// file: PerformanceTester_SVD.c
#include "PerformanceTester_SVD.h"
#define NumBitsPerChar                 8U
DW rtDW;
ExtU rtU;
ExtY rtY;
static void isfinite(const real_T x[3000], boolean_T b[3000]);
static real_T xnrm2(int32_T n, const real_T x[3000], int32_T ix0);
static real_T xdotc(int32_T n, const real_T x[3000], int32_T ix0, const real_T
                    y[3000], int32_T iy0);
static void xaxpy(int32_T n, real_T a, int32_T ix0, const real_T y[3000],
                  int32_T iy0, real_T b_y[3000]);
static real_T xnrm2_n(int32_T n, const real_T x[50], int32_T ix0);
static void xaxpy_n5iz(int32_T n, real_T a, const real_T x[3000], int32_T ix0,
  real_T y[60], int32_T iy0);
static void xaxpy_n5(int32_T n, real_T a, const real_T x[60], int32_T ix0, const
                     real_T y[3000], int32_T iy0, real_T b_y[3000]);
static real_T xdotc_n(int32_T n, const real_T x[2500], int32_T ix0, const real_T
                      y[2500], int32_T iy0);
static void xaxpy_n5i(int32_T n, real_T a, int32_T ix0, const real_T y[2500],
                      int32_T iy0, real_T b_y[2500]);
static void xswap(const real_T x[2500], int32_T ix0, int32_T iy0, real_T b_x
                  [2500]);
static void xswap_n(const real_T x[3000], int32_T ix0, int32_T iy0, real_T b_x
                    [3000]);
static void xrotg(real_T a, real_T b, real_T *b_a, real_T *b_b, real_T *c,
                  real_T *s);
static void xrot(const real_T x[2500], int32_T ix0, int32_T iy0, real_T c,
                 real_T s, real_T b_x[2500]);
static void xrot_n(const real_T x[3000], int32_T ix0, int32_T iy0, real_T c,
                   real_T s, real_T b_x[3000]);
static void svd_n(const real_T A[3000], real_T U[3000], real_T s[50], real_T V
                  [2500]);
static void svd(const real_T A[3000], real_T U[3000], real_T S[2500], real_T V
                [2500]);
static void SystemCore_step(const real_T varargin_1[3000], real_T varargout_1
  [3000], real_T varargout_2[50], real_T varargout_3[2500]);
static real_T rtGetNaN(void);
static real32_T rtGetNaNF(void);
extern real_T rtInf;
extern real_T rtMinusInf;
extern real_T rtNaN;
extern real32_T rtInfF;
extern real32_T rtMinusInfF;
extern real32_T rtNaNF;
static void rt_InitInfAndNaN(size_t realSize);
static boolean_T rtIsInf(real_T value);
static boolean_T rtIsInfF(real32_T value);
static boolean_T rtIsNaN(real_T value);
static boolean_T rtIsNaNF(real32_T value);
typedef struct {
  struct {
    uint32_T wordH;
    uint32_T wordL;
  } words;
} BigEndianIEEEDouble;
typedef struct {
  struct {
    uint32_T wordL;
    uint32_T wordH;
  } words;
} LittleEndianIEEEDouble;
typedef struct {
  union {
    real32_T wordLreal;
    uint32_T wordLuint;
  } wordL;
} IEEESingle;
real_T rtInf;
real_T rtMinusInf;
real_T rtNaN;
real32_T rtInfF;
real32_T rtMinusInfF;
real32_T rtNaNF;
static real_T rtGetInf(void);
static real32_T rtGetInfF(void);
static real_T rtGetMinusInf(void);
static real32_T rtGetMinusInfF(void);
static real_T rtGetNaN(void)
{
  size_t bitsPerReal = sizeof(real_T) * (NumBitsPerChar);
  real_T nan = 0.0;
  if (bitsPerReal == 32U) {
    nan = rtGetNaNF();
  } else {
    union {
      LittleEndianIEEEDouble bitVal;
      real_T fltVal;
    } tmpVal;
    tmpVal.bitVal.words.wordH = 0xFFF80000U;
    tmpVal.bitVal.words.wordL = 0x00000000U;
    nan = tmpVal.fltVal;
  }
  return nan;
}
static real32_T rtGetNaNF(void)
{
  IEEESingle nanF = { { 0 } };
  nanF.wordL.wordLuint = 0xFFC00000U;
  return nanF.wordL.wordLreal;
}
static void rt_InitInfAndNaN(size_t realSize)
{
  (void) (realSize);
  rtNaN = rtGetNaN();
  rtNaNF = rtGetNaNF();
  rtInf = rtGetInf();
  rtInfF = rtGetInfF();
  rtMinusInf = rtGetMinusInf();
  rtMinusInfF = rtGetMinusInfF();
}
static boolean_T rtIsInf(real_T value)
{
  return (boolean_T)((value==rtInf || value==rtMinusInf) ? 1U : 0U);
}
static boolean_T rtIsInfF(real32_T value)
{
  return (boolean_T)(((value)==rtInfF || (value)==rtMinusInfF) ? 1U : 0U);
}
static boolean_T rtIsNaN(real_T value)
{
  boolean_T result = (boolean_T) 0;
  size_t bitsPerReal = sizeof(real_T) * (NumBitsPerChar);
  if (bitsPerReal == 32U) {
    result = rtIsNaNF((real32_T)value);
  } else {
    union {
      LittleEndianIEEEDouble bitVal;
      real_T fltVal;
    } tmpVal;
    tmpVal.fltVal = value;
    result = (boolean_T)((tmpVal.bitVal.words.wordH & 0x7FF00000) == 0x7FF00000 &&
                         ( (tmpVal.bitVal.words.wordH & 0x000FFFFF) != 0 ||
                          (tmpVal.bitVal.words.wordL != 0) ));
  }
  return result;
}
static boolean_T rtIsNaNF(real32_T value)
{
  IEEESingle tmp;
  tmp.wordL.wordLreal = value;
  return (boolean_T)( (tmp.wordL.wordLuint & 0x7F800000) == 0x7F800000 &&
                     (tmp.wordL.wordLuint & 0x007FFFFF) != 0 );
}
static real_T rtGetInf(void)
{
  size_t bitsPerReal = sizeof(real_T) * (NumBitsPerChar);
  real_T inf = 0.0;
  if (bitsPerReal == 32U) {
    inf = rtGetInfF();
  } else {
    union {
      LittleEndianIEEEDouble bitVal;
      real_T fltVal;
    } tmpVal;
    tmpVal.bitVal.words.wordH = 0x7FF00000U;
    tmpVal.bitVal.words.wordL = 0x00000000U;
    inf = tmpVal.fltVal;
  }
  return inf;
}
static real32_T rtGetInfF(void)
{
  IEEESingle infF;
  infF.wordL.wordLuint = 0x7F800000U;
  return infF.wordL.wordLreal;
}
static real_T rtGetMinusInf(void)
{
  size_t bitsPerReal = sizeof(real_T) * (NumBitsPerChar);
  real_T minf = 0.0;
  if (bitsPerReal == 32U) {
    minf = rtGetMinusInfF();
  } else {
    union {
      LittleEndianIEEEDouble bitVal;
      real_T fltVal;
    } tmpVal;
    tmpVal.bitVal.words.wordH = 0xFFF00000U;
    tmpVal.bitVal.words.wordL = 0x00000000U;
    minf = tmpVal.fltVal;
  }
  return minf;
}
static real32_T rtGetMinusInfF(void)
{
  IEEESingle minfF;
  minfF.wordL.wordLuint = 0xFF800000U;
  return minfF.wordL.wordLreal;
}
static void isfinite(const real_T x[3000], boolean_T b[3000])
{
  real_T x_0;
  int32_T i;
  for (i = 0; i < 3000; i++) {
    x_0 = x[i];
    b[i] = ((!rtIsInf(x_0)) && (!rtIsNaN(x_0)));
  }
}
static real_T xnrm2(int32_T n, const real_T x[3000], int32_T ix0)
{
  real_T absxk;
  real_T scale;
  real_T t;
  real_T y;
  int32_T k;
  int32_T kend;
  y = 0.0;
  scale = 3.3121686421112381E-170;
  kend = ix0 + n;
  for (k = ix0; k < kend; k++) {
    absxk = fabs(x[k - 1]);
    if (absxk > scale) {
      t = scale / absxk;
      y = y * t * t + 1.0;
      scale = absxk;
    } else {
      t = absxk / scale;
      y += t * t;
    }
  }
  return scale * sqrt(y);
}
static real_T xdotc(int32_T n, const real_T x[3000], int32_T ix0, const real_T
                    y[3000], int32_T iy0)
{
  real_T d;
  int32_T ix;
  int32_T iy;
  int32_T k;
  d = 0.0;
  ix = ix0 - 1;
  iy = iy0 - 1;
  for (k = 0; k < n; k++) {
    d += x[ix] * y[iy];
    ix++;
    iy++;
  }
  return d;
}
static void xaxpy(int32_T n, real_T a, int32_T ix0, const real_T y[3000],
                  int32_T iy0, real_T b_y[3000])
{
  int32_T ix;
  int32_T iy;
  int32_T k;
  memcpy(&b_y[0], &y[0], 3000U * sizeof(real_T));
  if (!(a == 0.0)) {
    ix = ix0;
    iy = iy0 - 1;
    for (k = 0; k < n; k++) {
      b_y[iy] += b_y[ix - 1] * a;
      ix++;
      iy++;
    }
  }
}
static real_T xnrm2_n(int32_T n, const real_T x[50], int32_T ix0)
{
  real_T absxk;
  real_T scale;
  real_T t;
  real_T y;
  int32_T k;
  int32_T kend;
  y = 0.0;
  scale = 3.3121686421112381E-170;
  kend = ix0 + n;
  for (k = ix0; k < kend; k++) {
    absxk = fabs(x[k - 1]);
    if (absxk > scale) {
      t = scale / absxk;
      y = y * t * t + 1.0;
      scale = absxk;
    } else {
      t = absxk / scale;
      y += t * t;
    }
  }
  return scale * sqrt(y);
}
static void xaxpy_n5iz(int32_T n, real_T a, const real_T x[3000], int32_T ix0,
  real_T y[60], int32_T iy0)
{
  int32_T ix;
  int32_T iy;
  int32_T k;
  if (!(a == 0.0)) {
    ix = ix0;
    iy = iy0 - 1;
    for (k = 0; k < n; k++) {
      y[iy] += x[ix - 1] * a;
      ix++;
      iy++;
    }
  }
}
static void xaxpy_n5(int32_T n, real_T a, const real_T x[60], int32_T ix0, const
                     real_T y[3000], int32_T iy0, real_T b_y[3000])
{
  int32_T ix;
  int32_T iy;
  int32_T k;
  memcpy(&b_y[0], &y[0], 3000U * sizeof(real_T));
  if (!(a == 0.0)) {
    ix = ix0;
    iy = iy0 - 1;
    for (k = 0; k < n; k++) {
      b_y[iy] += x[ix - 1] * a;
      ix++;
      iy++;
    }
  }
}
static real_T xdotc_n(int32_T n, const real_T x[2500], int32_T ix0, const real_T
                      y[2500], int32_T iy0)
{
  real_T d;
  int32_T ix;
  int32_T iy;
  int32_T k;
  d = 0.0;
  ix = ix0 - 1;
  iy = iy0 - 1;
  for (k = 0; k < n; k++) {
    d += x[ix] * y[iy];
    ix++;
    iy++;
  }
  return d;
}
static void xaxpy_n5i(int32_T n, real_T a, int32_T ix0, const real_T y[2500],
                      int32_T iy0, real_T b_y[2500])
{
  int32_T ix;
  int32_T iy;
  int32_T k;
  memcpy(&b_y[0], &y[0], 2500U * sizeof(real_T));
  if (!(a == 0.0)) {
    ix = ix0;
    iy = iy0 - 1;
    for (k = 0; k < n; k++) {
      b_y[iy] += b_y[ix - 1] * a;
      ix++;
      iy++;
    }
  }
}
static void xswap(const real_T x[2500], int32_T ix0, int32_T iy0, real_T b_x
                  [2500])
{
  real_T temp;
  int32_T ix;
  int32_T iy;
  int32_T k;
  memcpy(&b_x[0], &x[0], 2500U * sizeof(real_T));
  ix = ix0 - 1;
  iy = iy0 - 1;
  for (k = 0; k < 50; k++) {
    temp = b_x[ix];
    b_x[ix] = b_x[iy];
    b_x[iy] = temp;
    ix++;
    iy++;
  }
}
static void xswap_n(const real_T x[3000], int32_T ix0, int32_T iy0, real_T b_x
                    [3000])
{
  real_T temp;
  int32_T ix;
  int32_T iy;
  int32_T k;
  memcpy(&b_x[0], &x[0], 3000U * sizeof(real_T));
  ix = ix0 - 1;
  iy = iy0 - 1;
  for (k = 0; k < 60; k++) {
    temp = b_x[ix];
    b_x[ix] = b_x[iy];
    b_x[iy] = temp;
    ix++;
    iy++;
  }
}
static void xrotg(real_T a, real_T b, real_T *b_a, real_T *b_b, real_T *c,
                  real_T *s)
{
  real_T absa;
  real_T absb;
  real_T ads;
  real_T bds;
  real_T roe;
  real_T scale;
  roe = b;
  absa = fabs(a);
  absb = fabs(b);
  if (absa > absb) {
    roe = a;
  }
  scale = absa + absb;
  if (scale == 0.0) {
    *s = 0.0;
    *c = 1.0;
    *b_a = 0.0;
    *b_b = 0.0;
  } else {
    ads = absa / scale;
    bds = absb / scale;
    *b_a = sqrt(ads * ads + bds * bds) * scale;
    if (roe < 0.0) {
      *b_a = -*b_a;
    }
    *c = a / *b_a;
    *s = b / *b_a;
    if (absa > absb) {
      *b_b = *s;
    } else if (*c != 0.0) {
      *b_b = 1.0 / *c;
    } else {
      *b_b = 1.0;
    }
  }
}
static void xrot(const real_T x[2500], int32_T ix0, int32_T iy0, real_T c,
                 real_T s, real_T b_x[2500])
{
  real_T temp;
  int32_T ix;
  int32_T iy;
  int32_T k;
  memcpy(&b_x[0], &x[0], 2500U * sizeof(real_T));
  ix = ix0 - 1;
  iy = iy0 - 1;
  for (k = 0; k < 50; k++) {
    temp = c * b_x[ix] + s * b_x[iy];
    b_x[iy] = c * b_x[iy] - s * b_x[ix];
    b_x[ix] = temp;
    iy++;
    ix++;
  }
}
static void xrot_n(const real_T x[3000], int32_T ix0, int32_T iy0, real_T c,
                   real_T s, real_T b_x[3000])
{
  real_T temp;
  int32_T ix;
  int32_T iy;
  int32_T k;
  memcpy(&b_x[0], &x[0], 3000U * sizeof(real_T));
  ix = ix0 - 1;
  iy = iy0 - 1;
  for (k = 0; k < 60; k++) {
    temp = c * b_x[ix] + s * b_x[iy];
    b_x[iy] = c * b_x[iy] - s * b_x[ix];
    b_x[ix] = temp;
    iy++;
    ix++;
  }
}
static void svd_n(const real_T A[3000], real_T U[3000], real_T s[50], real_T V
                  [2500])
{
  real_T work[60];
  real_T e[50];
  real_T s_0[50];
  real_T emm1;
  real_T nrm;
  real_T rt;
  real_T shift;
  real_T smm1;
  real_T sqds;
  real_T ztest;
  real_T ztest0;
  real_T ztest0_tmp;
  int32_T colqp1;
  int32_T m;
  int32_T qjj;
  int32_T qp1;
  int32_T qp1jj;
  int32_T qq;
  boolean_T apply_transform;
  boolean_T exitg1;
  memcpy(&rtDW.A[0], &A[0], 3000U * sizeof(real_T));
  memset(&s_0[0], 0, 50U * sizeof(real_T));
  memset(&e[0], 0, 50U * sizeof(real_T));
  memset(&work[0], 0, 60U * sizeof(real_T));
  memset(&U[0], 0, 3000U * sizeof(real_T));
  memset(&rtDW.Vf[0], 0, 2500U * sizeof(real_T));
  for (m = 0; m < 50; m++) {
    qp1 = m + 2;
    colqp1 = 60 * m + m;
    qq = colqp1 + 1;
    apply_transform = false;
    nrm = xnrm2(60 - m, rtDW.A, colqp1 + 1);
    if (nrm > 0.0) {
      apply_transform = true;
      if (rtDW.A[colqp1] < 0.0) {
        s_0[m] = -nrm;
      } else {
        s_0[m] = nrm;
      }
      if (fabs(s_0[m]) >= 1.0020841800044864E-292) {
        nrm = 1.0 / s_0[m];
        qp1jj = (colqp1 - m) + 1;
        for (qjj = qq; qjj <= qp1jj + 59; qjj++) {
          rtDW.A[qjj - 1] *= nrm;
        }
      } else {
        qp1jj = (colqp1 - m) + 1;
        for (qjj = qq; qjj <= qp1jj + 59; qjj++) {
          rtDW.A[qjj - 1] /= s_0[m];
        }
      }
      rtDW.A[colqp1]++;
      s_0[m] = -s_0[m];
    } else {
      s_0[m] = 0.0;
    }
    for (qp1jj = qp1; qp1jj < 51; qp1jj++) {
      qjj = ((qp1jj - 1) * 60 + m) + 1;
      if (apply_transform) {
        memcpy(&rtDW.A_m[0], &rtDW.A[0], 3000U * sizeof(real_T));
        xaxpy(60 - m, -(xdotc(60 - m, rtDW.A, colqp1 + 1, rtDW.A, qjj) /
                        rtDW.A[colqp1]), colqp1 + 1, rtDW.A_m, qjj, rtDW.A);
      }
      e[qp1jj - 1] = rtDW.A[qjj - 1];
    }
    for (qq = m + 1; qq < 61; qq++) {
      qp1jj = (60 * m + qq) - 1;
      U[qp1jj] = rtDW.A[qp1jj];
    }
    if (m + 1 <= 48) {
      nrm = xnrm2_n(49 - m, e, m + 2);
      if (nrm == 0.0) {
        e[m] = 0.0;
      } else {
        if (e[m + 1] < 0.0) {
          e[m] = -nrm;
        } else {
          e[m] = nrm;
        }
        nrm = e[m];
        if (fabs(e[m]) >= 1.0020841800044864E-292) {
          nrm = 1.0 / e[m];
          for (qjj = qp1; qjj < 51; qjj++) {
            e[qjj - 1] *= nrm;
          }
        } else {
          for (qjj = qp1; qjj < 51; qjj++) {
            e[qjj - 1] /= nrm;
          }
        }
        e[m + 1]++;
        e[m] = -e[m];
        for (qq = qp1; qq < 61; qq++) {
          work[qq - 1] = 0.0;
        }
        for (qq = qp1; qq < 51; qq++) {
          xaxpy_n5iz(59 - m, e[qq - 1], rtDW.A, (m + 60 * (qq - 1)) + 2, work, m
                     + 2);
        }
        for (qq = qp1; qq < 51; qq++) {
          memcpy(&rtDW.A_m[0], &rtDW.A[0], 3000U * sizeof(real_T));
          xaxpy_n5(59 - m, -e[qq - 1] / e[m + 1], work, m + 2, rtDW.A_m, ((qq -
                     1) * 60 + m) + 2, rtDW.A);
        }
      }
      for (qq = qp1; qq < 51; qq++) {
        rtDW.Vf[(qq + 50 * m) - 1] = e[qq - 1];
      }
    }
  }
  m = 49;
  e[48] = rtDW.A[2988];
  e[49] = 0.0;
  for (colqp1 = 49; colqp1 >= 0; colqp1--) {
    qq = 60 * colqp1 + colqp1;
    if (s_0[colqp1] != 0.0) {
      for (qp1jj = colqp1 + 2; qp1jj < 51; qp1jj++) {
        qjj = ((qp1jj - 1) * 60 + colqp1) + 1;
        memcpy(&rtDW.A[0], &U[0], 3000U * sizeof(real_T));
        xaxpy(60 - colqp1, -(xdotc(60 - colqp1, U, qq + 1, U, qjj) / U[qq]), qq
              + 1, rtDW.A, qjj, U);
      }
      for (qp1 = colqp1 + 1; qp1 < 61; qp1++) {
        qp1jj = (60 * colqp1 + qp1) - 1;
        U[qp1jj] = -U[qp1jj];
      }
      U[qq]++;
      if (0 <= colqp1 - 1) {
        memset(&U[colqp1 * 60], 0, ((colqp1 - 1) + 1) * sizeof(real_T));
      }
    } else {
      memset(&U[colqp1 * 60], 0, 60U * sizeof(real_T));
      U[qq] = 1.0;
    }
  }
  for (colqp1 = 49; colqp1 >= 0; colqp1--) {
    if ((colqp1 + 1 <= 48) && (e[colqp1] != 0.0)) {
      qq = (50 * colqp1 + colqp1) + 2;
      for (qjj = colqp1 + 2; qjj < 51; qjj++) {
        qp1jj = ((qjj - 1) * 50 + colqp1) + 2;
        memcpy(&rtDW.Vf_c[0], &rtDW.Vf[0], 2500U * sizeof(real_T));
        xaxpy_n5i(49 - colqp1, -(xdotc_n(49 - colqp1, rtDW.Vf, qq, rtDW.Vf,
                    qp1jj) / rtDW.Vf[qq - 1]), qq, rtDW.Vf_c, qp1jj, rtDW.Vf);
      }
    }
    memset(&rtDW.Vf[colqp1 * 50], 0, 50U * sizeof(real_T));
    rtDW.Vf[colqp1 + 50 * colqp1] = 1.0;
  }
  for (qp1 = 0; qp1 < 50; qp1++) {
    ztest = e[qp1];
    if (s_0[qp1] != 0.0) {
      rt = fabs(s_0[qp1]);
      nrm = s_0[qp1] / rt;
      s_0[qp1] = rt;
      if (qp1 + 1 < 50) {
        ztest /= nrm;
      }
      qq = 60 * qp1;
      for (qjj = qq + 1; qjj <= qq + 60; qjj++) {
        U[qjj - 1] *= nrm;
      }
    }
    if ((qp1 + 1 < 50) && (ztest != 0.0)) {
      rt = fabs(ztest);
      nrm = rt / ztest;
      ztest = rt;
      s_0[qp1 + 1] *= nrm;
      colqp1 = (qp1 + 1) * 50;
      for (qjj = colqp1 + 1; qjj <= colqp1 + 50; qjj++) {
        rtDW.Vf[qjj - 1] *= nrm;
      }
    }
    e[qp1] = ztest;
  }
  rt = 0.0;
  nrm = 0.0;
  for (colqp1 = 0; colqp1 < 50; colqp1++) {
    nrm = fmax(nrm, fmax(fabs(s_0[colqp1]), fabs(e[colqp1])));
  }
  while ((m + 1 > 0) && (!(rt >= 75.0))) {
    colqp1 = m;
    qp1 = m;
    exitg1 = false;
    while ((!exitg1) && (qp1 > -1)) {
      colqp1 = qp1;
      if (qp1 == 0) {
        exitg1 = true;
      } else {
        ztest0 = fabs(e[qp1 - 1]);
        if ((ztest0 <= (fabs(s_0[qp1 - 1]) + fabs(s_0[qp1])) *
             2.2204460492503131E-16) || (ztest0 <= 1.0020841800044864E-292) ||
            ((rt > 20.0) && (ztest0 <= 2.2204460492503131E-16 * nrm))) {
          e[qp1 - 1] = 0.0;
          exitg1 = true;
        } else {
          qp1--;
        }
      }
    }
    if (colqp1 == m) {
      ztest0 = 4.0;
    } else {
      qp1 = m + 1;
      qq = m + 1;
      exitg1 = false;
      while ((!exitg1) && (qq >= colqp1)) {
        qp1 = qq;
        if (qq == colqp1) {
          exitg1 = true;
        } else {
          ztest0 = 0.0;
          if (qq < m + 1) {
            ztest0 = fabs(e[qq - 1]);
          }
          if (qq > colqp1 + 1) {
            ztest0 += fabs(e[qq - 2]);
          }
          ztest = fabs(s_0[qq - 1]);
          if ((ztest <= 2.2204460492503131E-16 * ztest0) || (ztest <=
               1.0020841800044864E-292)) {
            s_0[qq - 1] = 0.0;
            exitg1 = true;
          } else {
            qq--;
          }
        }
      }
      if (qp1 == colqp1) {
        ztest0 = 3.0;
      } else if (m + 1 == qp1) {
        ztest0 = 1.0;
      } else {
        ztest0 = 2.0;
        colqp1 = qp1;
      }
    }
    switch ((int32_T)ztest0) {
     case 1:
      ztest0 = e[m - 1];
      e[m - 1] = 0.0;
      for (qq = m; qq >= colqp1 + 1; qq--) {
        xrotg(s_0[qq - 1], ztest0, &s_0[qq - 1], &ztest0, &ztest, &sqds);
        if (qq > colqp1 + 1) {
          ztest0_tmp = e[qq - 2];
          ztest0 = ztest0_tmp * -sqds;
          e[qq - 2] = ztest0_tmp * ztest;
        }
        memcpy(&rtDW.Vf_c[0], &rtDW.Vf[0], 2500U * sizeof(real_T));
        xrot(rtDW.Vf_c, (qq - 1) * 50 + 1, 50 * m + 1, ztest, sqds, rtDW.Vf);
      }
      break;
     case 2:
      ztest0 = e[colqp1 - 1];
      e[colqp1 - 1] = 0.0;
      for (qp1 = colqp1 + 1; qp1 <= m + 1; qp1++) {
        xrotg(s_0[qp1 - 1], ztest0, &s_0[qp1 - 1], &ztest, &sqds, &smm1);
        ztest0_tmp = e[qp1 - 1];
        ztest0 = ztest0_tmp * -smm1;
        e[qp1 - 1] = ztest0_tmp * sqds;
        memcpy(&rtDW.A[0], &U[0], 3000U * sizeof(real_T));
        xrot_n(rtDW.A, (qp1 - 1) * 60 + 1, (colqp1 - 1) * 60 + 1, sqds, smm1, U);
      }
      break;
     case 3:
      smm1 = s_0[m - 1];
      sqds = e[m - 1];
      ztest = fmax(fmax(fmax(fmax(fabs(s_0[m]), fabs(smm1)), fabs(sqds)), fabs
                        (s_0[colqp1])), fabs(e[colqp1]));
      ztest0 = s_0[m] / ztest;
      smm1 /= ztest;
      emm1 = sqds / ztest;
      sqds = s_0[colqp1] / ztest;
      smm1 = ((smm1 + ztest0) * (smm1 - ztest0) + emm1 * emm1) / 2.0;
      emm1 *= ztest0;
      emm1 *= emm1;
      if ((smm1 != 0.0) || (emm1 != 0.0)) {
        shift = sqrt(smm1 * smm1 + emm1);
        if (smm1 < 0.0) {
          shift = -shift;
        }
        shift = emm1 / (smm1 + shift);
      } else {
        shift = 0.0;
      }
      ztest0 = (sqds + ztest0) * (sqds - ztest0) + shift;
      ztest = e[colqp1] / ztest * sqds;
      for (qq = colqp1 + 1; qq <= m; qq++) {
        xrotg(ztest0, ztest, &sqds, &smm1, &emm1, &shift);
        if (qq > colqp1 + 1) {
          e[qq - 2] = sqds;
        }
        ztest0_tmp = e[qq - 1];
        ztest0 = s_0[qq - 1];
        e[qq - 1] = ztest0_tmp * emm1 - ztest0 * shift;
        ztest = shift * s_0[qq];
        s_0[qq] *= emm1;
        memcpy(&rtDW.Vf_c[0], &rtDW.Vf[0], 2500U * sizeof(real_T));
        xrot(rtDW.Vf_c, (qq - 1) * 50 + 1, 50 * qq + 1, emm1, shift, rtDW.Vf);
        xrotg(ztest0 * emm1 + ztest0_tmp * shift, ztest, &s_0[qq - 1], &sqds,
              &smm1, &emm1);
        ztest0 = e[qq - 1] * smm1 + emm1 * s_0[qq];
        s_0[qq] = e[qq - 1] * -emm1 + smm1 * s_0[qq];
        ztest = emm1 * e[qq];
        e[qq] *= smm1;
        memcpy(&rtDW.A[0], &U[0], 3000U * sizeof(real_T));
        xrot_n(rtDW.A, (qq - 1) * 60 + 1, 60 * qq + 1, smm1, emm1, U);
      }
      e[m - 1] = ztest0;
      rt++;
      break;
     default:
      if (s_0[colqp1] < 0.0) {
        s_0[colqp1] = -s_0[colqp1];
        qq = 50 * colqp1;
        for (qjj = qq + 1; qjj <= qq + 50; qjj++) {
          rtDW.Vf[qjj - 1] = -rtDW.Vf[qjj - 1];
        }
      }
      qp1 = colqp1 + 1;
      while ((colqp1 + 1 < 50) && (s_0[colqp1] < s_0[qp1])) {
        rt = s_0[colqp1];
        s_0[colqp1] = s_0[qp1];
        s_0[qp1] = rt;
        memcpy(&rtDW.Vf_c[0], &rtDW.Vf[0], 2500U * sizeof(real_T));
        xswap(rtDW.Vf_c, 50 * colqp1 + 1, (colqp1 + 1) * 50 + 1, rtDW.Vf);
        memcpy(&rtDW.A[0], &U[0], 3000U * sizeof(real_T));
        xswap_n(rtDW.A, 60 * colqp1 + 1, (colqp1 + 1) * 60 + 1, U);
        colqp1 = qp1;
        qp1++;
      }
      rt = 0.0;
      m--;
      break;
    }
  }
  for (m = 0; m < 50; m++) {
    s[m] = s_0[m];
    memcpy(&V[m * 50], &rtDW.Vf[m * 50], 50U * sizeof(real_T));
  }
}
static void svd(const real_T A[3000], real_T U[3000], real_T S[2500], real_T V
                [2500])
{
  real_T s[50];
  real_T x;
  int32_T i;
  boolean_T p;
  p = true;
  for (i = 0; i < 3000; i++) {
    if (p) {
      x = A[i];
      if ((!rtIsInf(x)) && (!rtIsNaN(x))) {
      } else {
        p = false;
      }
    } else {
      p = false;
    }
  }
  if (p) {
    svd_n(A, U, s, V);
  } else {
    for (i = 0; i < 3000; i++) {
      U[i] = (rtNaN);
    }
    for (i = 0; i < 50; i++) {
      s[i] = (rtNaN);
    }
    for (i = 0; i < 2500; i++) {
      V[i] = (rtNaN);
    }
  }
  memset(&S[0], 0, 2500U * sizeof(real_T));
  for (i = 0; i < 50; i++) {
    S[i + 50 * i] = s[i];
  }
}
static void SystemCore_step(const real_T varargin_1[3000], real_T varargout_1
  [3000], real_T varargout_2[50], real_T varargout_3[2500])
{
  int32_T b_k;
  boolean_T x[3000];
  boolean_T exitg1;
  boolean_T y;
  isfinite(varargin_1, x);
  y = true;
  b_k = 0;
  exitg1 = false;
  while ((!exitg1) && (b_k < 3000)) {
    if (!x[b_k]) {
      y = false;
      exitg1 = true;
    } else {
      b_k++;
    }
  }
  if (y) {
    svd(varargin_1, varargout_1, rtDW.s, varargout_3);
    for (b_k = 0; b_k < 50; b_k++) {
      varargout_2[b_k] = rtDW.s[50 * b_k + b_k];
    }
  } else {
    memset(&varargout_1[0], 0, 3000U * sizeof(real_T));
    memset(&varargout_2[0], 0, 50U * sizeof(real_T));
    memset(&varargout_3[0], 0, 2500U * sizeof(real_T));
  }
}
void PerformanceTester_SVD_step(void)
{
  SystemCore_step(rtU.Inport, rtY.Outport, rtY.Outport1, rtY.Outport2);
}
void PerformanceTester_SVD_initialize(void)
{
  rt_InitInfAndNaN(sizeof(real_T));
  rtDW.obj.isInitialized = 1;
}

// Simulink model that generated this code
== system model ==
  Inport : Inport
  Outport : Outport  <- 1: SingularValueDecomposition#1
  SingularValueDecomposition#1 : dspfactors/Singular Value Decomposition  <- 1: Inport
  Outport1 : Outport  <- 1: SingularValueDecomposition#1/2
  Outport2 : Outport  <- 1: SingularValueDecomposition#1/3
